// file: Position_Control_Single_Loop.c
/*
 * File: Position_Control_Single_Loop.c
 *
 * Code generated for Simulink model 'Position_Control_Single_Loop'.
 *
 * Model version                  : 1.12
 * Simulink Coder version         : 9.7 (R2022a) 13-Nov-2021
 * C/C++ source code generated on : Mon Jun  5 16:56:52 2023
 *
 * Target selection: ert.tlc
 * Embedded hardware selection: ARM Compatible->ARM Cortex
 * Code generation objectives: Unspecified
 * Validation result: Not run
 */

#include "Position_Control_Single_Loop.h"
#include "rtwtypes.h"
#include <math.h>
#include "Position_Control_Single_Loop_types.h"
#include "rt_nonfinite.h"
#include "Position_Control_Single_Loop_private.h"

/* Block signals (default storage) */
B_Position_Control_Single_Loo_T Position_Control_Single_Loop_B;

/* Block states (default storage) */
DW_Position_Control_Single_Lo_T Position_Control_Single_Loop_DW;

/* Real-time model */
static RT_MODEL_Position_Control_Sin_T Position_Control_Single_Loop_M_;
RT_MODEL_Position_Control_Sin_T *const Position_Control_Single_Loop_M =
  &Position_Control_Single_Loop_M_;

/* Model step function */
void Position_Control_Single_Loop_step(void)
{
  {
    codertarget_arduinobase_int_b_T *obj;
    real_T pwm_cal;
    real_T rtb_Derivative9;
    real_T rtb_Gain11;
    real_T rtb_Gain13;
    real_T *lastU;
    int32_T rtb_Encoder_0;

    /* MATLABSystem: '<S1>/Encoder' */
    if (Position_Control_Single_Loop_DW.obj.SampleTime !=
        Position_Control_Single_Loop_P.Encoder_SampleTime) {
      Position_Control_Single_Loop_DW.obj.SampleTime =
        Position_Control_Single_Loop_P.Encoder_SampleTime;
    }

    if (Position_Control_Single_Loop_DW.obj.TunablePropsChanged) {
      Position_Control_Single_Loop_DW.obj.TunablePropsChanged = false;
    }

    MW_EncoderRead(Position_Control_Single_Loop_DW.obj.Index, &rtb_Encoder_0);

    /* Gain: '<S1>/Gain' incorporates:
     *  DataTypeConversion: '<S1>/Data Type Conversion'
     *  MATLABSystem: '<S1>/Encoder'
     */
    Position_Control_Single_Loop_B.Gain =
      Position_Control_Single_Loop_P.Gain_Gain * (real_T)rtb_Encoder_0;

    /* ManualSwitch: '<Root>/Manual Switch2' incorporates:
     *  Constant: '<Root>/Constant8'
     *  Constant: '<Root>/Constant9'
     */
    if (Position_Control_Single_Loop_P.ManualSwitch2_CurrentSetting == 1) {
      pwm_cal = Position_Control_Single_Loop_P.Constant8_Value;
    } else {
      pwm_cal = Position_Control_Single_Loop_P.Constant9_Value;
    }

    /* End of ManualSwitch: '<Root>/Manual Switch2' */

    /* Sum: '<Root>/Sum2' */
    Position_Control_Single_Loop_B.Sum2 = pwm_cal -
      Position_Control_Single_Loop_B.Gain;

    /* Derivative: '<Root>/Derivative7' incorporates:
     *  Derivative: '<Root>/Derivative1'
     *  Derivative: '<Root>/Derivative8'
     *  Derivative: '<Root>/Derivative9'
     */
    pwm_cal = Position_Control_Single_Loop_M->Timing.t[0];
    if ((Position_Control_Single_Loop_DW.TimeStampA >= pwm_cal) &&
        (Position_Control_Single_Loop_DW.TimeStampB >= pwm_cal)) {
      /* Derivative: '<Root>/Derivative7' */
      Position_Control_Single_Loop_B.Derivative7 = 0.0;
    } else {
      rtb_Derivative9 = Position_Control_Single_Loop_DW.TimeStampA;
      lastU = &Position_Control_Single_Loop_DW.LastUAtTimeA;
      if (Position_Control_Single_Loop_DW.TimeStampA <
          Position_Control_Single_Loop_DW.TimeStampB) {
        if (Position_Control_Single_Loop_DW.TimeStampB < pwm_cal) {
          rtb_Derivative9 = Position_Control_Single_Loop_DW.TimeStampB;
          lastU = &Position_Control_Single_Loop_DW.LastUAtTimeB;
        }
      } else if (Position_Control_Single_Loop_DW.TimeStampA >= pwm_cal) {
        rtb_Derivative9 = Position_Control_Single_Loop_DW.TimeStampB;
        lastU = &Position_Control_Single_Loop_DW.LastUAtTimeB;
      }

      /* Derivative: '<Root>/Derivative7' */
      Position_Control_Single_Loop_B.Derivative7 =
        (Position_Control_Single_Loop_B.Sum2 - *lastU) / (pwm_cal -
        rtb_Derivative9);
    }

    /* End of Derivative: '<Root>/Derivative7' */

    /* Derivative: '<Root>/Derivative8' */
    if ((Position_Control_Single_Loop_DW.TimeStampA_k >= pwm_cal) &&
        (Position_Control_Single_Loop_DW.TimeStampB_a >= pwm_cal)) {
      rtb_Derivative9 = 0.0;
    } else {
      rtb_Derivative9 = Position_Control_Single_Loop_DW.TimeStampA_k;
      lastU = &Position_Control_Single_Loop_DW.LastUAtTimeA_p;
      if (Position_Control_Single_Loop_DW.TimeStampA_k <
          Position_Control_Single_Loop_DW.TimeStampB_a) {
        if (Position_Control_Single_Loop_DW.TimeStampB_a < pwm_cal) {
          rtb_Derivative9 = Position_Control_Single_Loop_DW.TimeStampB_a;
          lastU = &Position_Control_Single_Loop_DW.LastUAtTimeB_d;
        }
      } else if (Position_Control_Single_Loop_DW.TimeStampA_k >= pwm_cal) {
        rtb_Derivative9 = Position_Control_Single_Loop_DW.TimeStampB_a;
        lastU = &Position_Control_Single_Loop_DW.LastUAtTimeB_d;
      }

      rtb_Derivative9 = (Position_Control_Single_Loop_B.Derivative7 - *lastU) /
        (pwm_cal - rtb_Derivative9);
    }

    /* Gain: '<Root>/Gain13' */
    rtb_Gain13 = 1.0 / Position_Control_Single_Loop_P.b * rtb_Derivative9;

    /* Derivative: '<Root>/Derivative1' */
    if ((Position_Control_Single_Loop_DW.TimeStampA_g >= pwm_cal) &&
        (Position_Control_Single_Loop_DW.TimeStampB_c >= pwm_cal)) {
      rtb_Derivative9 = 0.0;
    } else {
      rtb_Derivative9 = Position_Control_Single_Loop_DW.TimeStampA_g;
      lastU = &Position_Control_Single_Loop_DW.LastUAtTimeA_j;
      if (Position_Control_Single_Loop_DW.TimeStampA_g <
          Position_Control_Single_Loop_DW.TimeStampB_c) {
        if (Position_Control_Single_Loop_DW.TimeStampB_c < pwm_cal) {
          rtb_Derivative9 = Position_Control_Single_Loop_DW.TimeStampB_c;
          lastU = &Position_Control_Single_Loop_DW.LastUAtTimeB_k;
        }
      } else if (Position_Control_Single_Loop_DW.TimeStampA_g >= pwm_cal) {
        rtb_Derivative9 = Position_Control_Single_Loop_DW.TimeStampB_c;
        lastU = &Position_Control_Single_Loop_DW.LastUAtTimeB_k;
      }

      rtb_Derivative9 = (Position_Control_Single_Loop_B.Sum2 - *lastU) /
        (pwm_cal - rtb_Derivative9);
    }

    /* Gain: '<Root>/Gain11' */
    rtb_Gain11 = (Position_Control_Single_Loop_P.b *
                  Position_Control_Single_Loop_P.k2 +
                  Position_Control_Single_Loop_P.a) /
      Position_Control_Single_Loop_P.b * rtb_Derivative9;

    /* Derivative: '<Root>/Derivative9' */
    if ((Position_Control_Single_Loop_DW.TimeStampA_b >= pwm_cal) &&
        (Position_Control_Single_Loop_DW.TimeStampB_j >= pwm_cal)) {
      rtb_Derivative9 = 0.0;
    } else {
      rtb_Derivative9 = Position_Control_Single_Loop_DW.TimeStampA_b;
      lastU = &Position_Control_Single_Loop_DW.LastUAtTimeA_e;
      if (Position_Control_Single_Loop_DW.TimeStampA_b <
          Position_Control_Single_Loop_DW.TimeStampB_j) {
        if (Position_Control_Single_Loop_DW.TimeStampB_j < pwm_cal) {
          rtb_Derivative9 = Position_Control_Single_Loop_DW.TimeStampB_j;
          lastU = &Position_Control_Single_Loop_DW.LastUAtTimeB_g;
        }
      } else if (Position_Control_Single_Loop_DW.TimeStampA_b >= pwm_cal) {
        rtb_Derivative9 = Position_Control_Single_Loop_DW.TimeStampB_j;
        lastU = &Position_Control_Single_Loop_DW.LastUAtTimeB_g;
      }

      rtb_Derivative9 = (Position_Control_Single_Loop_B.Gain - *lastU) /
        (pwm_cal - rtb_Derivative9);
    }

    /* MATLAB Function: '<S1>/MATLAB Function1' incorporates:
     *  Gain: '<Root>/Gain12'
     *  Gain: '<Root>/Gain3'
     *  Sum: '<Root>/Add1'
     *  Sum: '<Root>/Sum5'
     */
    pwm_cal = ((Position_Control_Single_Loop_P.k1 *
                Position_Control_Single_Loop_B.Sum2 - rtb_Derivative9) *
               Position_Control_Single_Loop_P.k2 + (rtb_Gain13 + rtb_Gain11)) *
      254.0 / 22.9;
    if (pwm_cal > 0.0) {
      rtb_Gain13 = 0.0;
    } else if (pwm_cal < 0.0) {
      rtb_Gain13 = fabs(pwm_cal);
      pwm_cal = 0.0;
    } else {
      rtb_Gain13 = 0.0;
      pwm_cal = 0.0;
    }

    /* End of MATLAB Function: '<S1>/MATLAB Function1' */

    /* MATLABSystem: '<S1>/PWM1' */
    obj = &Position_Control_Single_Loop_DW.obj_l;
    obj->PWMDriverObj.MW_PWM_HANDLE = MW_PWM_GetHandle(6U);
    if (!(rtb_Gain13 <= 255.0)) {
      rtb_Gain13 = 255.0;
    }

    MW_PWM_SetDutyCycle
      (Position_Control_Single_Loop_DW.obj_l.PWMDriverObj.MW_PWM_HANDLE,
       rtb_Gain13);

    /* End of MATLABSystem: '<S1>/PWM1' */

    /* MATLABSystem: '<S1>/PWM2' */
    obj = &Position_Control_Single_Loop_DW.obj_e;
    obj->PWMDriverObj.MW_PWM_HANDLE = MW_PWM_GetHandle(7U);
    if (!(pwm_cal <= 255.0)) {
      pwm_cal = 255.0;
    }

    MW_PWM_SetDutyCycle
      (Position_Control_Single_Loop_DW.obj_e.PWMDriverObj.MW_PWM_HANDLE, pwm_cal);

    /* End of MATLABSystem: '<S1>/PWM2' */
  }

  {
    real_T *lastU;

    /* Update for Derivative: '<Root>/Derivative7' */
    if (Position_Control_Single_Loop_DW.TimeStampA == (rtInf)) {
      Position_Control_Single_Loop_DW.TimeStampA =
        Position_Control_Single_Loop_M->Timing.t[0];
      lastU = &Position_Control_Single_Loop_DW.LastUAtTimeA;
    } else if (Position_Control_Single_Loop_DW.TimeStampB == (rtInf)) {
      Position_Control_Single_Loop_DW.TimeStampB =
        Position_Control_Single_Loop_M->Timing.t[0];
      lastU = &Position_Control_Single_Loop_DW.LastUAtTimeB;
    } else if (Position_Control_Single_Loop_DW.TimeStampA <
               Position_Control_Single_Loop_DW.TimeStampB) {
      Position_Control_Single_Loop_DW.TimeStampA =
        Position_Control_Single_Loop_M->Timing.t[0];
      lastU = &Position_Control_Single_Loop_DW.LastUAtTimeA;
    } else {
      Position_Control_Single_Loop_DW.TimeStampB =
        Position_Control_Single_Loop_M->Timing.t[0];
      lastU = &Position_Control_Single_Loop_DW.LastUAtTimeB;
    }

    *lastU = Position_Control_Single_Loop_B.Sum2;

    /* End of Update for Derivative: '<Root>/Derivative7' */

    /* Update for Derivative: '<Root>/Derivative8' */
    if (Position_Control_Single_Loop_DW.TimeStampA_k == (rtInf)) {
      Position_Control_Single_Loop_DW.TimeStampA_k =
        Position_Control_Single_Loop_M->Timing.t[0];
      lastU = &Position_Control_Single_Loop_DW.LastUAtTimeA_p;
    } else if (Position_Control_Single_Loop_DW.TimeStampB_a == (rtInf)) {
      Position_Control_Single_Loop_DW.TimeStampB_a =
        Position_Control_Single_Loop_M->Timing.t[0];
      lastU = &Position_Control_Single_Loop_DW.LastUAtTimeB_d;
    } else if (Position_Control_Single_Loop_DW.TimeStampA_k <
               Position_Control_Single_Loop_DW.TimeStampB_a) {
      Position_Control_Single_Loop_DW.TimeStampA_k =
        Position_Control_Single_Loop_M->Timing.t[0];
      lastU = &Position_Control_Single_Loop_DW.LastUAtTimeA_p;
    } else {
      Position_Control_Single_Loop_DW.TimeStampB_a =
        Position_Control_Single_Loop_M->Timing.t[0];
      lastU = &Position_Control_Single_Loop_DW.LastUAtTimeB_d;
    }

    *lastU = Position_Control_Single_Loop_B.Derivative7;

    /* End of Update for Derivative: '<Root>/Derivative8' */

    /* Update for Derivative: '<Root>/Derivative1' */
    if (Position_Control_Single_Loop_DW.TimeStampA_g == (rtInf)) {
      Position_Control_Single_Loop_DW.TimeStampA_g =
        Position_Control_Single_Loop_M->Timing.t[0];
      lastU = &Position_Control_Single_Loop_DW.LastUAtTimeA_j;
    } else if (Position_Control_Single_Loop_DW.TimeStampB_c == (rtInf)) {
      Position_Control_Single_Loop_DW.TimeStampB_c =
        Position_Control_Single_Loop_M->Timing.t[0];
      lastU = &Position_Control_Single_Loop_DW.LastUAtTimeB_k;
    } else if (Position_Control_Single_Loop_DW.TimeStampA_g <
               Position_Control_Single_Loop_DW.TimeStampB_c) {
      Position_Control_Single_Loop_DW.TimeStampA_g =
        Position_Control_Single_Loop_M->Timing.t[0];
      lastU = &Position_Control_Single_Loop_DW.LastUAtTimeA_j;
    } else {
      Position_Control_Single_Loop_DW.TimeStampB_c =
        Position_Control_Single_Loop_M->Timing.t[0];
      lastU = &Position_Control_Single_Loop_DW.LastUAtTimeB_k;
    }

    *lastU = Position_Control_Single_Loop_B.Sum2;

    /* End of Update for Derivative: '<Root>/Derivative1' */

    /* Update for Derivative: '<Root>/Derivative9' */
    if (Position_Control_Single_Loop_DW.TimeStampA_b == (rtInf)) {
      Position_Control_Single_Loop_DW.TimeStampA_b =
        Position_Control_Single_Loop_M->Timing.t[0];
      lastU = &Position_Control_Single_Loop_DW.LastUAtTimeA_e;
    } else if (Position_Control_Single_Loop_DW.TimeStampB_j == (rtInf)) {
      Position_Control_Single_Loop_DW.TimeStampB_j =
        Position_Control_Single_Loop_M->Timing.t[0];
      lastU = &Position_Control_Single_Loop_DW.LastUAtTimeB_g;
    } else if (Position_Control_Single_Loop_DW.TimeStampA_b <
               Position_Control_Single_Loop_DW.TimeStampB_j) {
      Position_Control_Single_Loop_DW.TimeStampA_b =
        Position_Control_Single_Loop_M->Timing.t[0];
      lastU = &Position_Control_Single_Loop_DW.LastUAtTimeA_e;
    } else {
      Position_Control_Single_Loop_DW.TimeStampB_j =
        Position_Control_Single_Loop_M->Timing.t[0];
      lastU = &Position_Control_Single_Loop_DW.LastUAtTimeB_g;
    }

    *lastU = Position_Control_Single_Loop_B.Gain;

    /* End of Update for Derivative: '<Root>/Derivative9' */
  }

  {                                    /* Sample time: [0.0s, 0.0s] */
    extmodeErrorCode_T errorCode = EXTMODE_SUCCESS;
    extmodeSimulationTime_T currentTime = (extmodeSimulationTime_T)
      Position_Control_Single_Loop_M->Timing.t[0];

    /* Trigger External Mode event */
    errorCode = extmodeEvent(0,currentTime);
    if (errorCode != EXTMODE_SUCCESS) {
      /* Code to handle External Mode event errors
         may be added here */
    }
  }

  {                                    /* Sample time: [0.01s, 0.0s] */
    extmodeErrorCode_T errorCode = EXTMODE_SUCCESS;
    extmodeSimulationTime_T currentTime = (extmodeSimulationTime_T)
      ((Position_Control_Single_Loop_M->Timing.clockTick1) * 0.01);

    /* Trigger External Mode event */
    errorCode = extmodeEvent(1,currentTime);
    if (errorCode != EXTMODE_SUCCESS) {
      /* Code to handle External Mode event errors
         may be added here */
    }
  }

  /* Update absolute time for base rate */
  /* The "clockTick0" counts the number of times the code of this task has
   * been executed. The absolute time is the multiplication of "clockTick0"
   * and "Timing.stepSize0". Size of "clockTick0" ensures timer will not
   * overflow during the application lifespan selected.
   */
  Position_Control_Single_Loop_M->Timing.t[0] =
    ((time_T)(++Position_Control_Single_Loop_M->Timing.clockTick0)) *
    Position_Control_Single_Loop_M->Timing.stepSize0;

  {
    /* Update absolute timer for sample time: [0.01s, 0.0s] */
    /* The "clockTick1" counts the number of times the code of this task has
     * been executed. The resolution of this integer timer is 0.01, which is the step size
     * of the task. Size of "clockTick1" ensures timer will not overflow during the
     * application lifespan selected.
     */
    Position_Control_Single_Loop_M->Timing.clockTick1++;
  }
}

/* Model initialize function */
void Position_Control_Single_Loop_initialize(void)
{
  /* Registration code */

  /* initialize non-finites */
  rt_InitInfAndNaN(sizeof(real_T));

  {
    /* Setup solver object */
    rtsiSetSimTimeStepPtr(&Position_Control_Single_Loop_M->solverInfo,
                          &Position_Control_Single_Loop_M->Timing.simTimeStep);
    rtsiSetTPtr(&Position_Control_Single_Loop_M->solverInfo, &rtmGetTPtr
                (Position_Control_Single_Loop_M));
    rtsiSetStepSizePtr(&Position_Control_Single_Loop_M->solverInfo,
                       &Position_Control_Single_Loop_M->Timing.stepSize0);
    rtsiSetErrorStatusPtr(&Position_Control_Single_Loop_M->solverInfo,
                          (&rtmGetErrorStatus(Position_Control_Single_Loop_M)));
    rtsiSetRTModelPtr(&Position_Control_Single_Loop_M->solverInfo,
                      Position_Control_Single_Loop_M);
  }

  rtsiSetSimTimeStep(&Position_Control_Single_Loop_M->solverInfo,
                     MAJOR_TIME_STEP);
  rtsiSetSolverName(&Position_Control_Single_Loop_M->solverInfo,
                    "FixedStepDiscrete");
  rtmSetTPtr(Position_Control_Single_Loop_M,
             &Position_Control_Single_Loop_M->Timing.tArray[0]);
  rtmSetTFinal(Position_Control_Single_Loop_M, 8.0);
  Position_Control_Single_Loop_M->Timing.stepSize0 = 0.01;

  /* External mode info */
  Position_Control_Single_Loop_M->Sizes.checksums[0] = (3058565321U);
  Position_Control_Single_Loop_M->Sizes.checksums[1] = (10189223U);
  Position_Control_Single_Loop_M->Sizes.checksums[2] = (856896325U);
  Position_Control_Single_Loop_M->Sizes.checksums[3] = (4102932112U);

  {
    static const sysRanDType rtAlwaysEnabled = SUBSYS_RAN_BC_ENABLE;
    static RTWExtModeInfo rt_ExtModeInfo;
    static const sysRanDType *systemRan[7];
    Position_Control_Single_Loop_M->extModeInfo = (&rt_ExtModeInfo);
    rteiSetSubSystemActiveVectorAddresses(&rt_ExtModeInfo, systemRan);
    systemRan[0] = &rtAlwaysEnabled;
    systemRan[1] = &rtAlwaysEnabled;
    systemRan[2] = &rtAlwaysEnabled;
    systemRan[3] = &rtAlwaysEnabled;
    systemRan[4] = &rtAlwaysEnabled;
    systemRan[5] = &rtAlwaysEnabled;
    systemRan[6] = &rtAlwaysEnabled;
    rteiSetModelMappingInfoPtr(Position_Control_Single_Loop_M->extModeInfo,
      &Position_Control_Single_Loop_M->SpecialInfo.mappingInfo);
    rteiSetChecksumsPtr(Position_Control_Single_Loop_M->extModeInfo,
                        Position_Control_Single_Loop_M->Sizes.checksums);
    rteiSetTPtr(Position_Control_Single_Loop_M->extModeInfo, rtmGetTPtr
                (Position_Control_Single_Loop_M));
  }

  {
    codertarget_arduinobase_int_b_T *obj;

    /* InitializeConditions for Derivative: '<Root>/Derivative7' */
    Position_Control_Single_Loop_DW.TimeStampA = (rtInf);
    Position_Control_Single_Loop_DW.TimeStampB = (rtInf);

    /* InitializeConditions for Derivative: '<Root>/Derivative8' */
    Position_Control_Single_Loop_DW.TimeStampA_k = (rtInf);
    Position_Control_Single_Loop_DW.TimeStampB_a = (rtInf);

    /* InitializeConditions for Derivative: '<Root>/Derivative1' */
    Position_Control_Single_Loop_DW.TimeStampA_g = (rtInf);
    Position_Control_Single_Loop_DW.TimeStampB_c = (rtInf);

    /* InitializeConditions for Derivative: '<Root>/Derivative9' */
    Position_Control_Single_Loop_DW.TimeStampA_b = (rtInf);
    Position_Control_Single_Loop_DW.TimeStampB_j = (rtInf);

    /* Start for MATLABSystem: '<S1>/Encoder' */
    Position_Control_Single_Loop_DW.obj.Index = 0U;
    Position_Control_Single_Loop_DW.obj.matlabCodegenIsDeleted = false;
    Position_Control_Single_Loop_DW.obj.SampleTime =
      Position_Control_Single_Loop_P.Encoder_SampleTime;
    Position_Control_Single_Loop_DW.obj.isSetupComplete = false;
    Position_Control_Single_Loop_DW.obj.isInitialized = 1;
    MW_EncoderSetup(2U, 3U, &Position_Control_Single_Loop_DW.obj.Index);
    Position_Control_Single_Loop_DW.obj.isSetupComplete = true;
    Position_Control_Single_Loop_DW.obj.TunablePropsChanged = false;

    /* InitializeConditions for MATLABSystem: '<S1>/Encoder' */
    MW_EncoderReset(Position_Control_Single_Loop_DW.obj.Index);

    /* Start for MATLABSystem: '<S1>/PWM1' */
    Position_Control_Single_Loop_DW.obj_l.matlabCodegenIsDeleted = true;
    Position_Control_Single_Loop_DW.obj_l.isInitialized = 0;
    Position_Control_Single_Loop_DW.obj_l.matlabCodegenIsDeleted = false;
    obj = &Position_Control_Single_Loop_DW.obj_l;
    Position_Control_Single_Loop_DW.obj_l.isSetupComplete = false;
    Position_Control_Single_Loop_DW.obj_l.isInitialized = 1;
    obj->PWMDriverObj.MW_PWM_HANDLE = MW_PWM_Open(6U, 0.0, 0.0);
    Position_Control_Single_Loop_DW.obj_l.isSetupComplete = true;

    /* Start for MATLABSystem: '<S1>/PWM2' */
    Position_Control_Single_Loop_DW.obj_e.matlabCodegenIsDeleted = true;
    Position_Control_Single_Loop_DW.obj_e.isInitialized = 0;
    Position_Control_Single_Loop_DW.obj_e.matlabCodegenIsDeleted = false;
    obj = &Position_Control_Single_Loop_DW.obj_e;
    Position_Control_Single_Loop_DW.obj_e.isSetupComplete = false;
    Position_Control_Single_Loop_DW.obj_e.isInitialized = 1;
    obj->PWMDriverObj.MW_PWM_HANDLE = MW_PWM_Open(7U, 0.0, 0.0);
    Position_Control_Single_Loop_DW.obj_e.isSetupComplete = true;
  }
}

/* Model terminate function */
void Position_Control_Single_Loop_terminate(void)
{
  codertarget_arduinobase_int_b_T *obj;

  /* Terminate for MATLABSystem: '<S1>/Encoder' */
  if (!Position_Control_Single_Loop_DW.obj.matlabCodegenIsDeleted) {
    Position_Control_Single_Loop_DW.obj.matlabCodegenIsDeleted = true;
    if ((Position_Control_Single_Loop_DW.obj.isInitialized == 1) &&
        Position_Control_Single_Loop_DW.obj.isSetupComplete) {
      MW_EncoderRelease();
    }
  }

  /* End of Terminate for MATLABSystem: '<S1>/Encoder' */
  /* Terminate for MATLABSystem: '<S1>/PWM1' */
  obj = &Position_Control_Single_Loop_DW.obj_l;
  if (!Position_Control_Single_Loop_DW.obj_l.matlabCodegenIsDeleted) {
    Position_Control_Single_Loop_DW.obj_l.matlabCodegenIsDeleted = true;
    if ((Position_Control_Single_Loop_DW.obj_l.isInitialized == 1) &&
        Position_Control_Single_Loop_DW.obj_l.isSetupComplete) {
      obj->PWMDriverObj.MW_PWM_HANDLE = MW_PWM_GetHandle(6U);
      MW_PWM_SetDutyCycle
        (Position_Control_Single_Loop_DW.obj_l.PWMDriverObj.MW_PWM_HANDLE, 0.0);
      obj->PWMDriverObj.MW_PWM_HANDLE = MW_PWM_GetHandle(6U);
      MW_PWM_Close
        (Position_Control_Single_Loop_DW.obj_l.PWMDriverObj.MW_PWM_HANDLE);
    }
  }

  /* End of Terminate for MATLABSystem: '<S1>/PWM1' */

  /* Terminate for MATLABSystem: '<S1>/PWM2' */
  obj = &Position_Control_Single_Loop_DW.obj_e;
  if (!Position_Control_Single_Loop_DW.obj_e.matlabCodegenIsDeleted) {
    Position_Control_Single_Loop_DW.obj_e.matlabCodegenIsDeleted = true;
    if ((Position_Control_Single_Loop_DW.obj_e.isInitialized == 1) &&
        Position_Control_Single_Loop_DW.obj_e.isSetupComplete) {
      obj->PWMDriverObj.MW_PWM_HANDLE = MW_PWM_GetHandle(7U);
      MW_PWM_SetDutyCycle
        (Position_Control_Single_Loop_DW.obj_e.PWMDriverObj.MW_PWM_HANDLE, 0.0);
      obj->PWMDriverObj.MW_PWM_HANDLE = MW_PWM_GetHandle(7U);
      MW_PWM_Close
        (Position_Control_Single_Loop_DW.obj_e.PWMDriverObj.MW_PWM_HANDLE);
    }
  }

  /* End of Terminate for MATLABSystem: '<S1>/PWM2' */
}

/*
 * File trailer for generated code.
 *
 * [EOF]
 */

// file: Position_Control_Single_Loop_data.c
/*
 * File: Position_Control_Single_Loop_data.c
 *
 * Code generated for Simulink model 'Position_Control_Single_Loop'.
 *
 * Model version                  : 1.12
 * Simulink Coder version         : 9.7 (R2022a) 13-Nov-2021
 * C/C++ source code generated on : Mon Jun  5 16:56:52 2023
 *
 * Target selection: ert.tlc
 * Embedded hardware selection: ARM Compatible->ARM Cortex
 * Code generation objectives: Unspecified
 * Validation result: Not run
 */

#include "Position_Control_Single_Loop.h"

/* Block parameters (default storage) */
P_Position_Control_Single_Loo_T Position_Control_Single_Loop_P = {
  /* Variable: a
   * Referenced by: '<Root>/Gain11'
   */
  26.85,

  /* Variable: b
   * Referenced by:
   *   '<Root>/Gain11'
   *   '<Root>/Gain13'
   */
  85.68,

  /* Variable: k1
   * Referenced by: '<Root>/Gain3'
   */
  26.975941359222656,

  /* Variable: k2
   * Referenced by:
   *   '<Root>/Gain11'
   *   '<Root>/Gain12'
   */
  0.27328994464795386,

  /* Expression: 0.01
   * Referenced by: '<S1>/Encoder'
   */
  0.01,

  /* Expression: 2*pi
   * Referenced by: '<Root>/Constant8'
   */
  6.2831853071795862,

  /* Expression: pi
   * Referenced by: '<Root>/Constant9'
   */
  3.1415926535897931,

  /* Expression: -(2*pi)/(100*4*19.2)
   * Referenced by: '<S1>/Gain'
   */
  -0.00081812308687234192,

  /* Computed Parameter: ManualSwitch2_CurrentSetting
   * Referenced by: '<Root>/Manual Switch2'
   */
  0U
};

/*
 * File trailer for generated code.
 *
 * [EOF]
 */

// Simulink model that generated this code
simulink model "Position_Control_Single_Loop"  (R2022a)
settings: Solver=ode1  StartTime=0.0  StopTime=8  FixedStep=0.01  RelTol=1e-3  EnableMultiTasking=on
undefined symbols (not defined in the file or in its folder): a, b, k1, k2, kd4, kp4
libraries: arduinolib x8, arduinosensorlib x2

== system Position_Control_Single_Loop ==
  note: $\theta$
  note: $\theta$
  Add1 : Sum  Inputs=+++
  Add2 : Sum  Commented=on  Inputs=++++
  Constant5 : Constant  Commented=on  Value=2*pi
  Constant7 : Constant  Commented=on  Value=pi
  Constant8 : Constant  Value=2*pi
  Constant9 : Constant  Value=pi
  Derivative{1,7..9} (4 alike) : Derivative
  Derivative{2..5} (4 alike) : Derivative  Commented=on
  Gain11 : Gain  Gain=(a+b*k2)/b
  Gain12 : Gain  Gain=k2
  Gain13 : Gain  Gain=1/b
  Gain3 : Gain  Gain=k1
  Gain6 : Gain  Commented=on  Gain=kp4
  Gain7 : Gain  Commented=on  Gain=kd4
  Gain8 : Gain  Commented=on  Gain=a/b
  Gain9 : Gain  Commented=on  Gain=1/b
  Manual Switch1 : ManualSwitch  Commented=on
  Manual Switch2 : ManualSwitch  CurrentSetting=0
  Right motor1 : Subsystem
  Right motor2 : Subsystem  Commented=on
  Scope : Scope  Commented=on
  Scope1 : Scope
  Scope4 : Scope  Commented=on
  Scope7 : Scope
  Sum2 : Sum  Inputs=|+-
  Sum3 : Sum  Commented=on  Inputs=|+-
  Sum5 : Sum  Inputs=|+-
  wires:
  Constant7/1 -> Manual Switch1/2
  Constant5/1 -> Manual Switch1/1
  Gain7/1 -> Derivative2/1
  Gain8/1 -> Add2/2
  Derivative3/1 -> Gain8/1
  Derivative5/1 -> Gain9/1
  Right motor2/1(outGearBox) -> Sum3/2, Scope4/1
  Gain6/1 -> Add2/3
  Add2/1 -> Right motor2/1(v_a)
  Gain9/1 -> Add2/1
  Derivative2/1 -> Add2/4
  Sum3/1 -> Scope/1, Gain6/1, Gain7/1
  Derivative4/1 -> Derivative5/1
  Manual Switch1/1 -> Sum3/1, Derivative3/1, Derivative4/1
  Manual Switch2/1 -> Sum2/1
  Derivative9/1 -> Sum5/2
  Constant8/1 -> Manual Switch2/1
  Gain11/1 -> Add1/2
  Add1/1 -> Right motor1/1(v_a)
  Sum2/1 -> Scope1/1, Derivative7/1, Derivative1/1, Gain3/1
  Constant9/1 -> Manual Switch2/2
  Sum5/1 -> Gain12/1
  Derivative8/1 -> Gain13/1
  Gain13/1 -> Add1/1
  Right motor1/1(outGearBox) -> Sum2/2, Derivative9/1, Scope7/1
  Gain12/1 -> Add1/3
  Derivative7/1 -> Derivative8/1
  Gain3/1 -> Sum5/1
  Derivative1/1 -> Gain11/1

== system Position_Control_Single_Loop/Right motor1 ==
  v_a : Inport
  Convert pulse to rad1 : MATLAB Function  Commented=on  TreatAsAtomicUnit=on
  Data Type Conversion : DataTypeConversion  OutDataTypeStr=double  SaturateOnIntegerOverflow=off  RndMeth=Floor
  Digital Output : arduinolib/Digital Output  Commented=on  pinNumber=7  Direction=output  blockPlatform=arduino
  Encoder : arduinosensorlib/Encoder  InputA=2  InputB=3  Mode=No reset  SampleTime=0.01
  Encoder1 : S-Function  Commented=on  InitFcn=try, set_param(gcb,'FunctionName','readEncDUEpin8_9'), end  FunctionName=readEncDUEpin8_9  SFunctionModules=readEncDUEpin8_9_wrapper  SFunctionDeploymentMode=off  EnableBusSupport=off  mask(S-Function Builder){}
      mask help: Simulink:masks:SFunctionBuilder_MD
      mask init:
      | val = [[.9  0.75 0.75 1 1 .9 .9 1]',[1 1 0.75 0.75 .9 .9 1 .9]'];try , sys = get_param(gcb,'SfunBuilderFcnName');if isempty(sys), sys = get_param(gcb,'FunctionName'); end,catch, sys = get_param(gcb,'FunctionName'); end
  Gain : Gain  Gain=-(2*pi)/(100*4*19.2)
  MATLAB Function1 : MATLAB Function  TreatAsAtomicUnit=on
  MATLAB Function2 : MATLAB Function  Commented=on  TreatAsAtomicUnit=on
  PWM : arduinolib/PWM  Commented=on  pinNumber=5  frequencyType=Default  desiredFrequency=490.2  achievableFrequency=490.2
  PWM1 : arduinolib/PWM  pinNumber=6  frequencyType=Default  desiredFrequency=490.2  achievableFrequency=490.2
  PWM2 : arduinolib/PWM  pinNumber=7  frequencyType=Default  desiredFrequency=490.2  achievableFrequency=490.2
  Scope : Scope  Commented=on
  Scope1 : Scope
  gearRatio : Constant  Commented=on  Value=336
  totalPPR : Constant  Commented=on  Value=16*2
  outGearBox : Outport
  wires:
  Gain/1 -> Scope1/1, outGearBox/1
  Encoder/1 -> Data Type Conversion/1
  v_a/1 -> MATLAB Function1/1(v_a)
  MATLAB Function1/2(Rpwm) -> PWM2/1
  MATLAB Function1/1(Lpwm) -> PWM1/1
  Encoder1/1 -> Convert pulse to rad1/1(u)
  Convert pulse to rad1/1(outGearBox) -> Scope/1
  gearRatio/1 -> Convert pulse to rad1/3(gearRatio)
  MATLAB Function2/1(pwm) -> PWM/1
  MATLAB Function2/2(dir) -> Digital Output/1
  totalPPR/1 -> Convert pulse to rad1/2(ppr)
  Data Type Conversion/1 -> Gain/1

== system Position_Control_Single_Loop/Right motor2 ==
  v_a : Inport
  Convert pulse to rad1 : MATLAB Function  Commented=on  TreatAsAtomicUnit=on
  Digital Output : arduinolib/Digital Output  Commented=on  pinNumber=7  Direction=output  blockPlatform=arduino
  Encoder : arduinosensorlib/Encoder  InputA=2  InputB=3  Mode=No reset  SampleTime=0.01
  Encoder1 : S-Function  Commented=on  InitFcn=try, set_param(gcb,'FunctionName','readEncDUEpin8_9'), end  FunctionName=readEncDUEpin8_9  SFunctionModules=readEncDUEpin8_9_wrapper  SFunctionDeploymentMode=off  EnableBusSupport=off  mask(S-Function Builder){}
      mask help: Simulink:masks:SFunctionBuilder_MD
      mask init: same as Position_Control_Single_Loop/Right motor1/Encoder1
  Gain : Gain  Gain=-(2*pi)/(100*4*19.2)
  MATLAB Function1 : MATLAB Function  TreatAsAtomicUnit=on
  MATLAB Function2 : MATLAB Function  Commented=on  TreatAsAtomicUnit=on
  PWM : arduinolib/PWM  Commented=on  pinNumber=5  frequencyType=Default  desiredFrequency=490.2  achievableFrequency=490.2
  PWM1 : arduinolib/PWM  pinNumber=6  frequencyType=Default  desiredFrequency=490.2  achievableFrequency=490.2
  PWM2 : arduinolib/PWM  pinNumber=7  frequencyType=Default  desiredFrequency=490.2  achievableFrequency=490.2
  Scope : Scope  Commented=on
  Scope1 : Scope
  gearRatio : Constant  Commented=on  Value=336
  totalPPR : Constant  Commented=on  Value=16*2
  outGearBox : Outport
  wires:
  totalPPR/1 -> Convert pulse to rad1/2(ppr)
  MATLAB Function2/2(dir) -> Digital Output/1
  MATLAB Function2/1(pwm) -> PWM/1
  gearRatio/1 -> Convert pulse to rad1/3(gearRatio)
  Convert pulse to rad1/1(outGearBox) -> Scope/1
  Encoder1/1 -> Convert pulse to rad1/1(u)
  MATLAB Function1/1(Lpwm) -> PWM1/1
  MATLAB Function1/2(Rpwm) -> PWM2/1
  v_a/1 -> MATLAB Function1/1(v_a)
  Encoder/1 -> Gain/1
  Gain/1 -> Scope1/1, outGearBox/1

== matlab function Position_Control_Single_Loop/Right motor2/Convert pulse to rad1 ==
  settings: updateMethod=DISCRETE
function outGearBox = fcn(u,ppr,gearRatio)

persistent counter_num over_flag
if(isempty(counter_num)), counter_num = 0;end
if(isempty(over_flag)), over_flag = 0;end
pulse2radian = 2*pi/ppr; % 1 pulse = ?? radian

if(double(u) - counter_num > 40000), over_flag = over_flag-1;
elseif(double(u) - counter_num < -40000), over_flag = over_flag+1;
end

inGearBox = (double(u)+over_flag*(2^32 -1))*pulse2radian; 
outGearBox = inGearBox/gearRatio;
counter_num = double(u) ;

== matlab function Position_Control_Single_Loop/Right motor2/MATLAB Function2 ==
function [pwm,dir] = fcn(v_a)

vmax = 22.9;
%vmax = 10;
pwm_cal = v_a*254/vmax;
if pwm_cal > 0
    pwm = pwm_cal;
    dir = 0;
elseif pwm_cal < 0
    pwm = abs(pwm_cal);
    dir = 1;
else
    pwm = 0;
    dir = 0;
end

== matlab function Position_Control_Single_Loop/Right motor2/MATLAB Function1 ==
function [Lpwm,Rpwm] = fcn(v_a)

vmax = 22.9;
pwm_cal = v_a*254/vmax;

if pwm_cal > 0
    Lpwm = 0;
    Rpwm = pwm_cal;
elseif pwm_cal < 0
    Lpwm = abs(pwm_cal);
    Rpwm = 0;
else
    Lpwm = 0;
    Rpwm = 0;
end

== matlab function Position_Control_Single_Loop/Right motor1/Convert pulse to rad1 ==
  settings: updateMethod=DISCRETE
function outGearBox = fcn(u,ppr,gearRatio)

persistent counter_num over_flag
if(isempty(counter_num)), counter_num = 0;end
if(isempty(over_flag)), over_flag = 0;end
pulse2radian = 2*pi/ppr; % 1 pulse = ?? radian

if(double(u) - counter_num > 40000), over_flag = over_flag-1;
elseif(double(u) - counter_num < -40000), over_flag = over_flag+1;
end

inGearBox = (double(u)+over_flag*(2^32 -1))*pulse2radian; 
outGearBox = inGearBox/gearRatio;
counter_num = double(u) ;

== matlab function Position_Control_Single_Loop/Right motor1/MATLAB Function1 ==
function [Lpwm,Rpwm] = fcn(v_a)

vmax = 22.9;
pwm_cal = v_a*254/vmax;

if pwm_cal > 0
    Lpwm = 0;
    Rpwm = pwm_cal;
elseif pwm_cal < 0
    Lpwm = abs(pwm_cal);
    Rpwm = 0;
else
    Lpwm = 0;
    Rpwm = 0;
end

== matlab function Position_Control_Single_Loop/Right motor1/MATLAB Function2 ==
function [pwm,dir] = fcn(v_a)

vmax = 22.9;
%vmax = 10;
pwm_cal = v_a*254/vmax;
if pwm_cal > 0
    pwm = pwm_cal;
    dir = 0;
elseif pwm_cal < 0
    pwm = abs(pwm_cal);
    dir = 1;
else
    pwm = 0;
    dir = 0;
end
